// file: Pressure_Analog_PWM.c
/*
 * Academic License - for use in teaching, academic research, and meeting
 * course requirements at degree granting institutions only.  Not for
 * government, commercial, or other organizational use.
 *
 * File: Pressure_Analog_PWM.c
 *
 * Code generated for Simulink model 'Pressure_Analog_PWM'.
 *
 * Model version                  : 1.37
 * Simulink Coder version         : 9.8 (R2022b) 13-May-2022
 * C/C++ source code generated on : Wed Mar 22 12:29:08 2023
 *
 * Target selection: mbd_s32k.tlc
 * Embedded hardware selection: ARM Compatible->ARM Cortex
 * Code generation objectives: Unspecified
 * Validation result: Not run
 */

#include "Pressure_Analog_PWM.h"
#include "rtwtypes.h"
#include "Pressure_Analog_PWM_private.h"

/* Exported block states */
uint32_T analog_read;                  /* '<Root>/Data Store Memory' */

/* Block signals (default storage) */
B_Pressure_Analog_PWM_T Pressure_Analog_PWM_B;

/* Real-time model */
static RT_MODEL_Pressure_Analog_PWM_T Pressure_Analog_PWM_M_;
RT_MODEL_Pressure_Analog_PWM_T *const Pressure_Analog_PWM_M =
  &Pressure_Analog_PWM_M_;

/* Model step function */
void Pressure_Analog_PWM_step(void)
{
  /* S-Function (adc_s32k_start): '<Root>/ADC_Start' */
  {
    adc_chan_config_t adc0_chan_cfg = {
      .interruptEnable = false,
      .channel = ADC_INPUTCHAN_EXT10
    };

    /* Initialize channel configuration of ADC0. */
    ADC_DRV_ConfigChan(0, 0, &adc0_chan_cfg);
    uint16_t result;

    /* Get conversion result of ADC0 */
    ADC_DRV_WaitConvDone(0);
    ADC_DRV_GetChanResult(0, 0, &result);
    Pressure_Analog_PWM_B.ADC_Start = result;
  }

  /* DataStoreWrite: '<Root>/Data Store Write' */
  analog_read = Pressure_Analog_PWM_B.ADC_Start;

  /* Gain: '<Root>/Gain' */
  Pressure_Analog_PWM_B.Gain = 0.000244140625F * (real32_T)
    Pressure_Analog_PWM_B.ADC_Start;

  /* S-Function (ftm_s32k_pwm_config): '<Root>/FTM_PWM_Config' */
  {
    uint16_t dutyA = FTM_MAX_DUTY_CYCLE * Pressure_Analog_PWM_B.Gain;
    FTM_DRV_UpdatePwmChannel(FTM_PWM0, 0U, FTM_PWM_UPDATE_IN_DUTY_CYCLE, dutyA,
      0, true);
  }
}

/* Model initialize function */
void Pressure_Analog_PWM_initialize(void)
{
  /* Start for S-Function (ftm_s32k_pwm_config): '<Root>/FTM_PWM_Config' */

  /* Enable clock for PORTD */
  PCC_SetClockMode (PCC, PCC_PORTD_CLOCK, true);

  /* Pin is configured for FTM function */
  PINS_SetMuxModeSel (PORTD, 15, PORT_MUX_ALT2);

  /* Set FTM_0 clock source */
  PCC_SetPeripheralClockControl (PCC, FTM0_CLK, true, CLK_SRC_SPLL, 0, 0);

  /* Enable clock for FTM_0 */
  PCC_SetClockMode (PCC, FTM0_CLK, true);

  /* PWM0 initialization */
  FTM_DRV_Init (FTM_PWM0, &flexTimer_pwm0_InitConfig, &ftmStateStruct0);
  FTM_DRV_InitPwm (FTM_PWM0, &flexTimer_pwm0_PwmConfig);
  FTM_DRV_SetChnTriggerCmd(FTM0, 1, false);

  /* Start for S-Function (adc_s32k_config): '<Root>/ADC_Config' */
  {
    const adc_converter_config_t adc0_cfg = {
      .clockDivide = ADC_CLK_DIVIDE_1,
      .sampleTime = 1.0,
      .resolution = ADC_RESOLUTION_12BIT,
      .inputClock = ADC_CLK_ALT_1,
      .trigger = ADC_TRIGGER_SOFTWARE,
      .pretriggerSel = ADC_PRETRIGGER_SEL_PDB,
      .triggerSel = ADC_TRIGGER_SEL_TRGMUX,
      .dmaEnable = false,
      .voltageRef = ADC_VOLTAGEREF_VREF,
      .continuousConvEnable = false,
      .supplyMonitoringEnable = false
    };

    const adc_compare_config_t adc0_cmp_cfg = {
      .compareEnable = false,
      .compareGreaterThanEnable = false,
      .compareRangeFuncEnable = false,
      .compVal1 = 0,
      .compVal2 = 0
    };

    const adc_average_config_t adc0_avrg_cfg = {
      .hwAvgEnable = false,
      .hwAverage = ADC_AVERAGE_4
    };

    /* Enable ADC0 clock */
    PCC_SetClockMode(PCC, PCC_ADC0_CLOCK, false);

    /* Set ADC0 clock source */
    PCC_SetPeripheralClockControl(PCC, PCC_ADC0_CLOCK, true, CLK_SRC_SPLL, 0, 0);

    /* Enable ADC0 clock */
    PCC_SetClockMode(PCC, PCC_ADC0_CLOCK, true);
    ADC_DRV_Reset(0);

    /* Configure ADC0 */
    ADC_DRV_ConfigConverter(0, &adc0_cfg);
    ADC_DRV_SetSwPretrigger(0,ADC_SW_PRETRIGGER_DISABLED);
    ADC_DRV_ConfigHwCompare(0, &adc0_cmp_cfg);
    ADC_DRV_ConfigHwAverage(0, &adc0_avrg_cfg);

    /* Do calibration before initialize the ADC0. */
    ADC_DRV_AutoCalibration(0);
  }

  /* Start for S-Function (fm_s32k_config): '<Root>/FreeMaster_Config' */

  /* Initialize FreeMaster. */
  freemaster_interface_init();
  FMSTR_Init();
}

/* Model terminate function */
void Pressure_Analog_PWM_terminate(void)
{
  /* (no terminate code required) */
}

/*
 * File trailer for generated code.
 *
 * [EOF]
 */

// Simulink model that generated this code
simulink model "Pressure_Analog_PWM"  (R2022b)
settings: Solver=FixedStepDiscrete  StartTime=0.0  StopTime=10.0  RelTol=1e-3  EnableMultiTasking=on
InitFcn:
  | mbd_s32k_consistency_checks(bdroot(gcs));
model workspace (MAT data in the model file):
  mwTaskManagerKernelLatency = 1e-06
undefined symbols (not defined in the file): LQFP
libraries: mbd_s32k1xx_ec_toolbox x5

== system Pressure_Analog_PWM ==
  note: This algorithm reads the analog output from the pressure
      | sensor and changes the red LED intensity accordingly.
      | The read value can be visualized on FreeMaster through
      |  the variable "analog_read".
      |
      | Hardware Requirements:
      | - S32K144 board
      | - HTDM100BSP
      |
      | Pin connections:
      |
      | Sensor    |     Board
      |     1         |      PTC2
      |     2         |      GND
      |     3         |        5V
      |
      |
      | Kamilla Peixoto - Scaleo Medical
      | v1 - 22/03/2023
  note: Analog Reading
  note: Watched Variables
  note: Configuration
  ADC_Config : mbd_s32k1xx_ec_toolbox/Motor Control Blocks/ADC Blocks/ADC_Config  instance=0  mode=12-bit conversion  smplts=2  adiclk=alternate clock 1  adiv=input clock  show_adv_opts=on  pretrgsel=PDB pre-trigger  swpretrg=Disabled  adtrg=software  trgsel=TRGMUX output  refsel=Vrefh and Vrefl  supply_monitoring=off  acfe=off  acfgt=off  acren=off  cv1=0  cv2=0  adco=off  avge=off  avgs=4 samples
  ADC_Start : mbd_s32k1xx_ec_toolbox/Motor Control Blocks/ADC Blocks/ADC_Start  instance=0  adc_r=A  adc_chan=PTC2: [ADC0_SE10 | ADC Single Ended Input]  aien=off  mcuTargetUpdate=on
  Data Store Memory : DataStoreMemory  DataStoreName=analog_read  WriteAfterWriteMsg=warning  ShowAdditionalParam=off  StateMustResolveToSignalObject=on
  Data Store Write : DataStoreWrite  DataStoreName=analog_read  IndexOptions=Index vector (dialog)  Indices=1  OutputSizes=1
  FTM_PWM_Config : mbd_s32k1xx_ec_toolbox/Motor Control Blocks/FTM Blocks/FTM_PWM_Config  ftmModule=0  ftmMode=Edge-Aligned PWM  ftmSourceClock=80 MHz  swcontrol_enable=off  chan0En=on  chan0Type=Complementary  chan2En=off  chan2Type=Independent  chan4En=off  chan4Type=Independent  chan6En=off  chan6Type=Independent  ftmPwmUnits=Hz  outFrequency=10000  ftmPeriod=8000  ftmPrescaler=Divide by 1  deadtimeUnits=Nanoseconds  deadtimeNs=0  deadtimeTicks=0  deadtimePrescaler=Divide by 1  dutyCycleCh0=0.25  dutyCycleCh1=0.25  dutyCycleCh2=0.25  dutyCycleCh3=0.25  dutyCycleCh4=0.25  dutyCycleCh5=0.25  dutyCycleCh6=0.25  dutyCycleCh7=0.25  dutyCycleSim=off  startAfterInit=on  showAdvOpt=on  pinFtmCh0=PTD15: [FTM0_CH0 | FTM Channel]  pinFtmCh1=None  pinPolCh0=Active Low  pinPolCh1=Active Low  outputComplem0=Main duplicated  outputLevel0=Low  outputLevel1=Low  pinFtmCh2=PTD0: [FTM0_CH2 | FTM Channel]  pinFtmCh3=None  pinPolCh2=Active Low  pinPolCh3=Active Low  outputComplem2=Main duplicated  outputLevel2=Low  outputLevel3=Low  pinFtmCh4=PTB4: [FTM0_CH4 | FTM Channel]  pinFtmCh5=None  pinPolCh4=Active Low  pinPolCh5=Active Low  outputComplem4=Main duplicated  outputLevel4=Low  outputLevel5=Low  pinFtmCh6=PTA17: [FTM0_CH6 | FTM Channel]  pinFtmCh7=None  pinPolCh6=Active Low  pinPolCh7=Active Low  outputComplem6=Main duplicated  outputLevel6=Low  outputLevel7=Low  initTrigger=off  chTrigger0=off  chTrigger1=off  chTrigger2=off  chTrigger3=off  chTrigger4=off  chTrigger5=off  chTrigger6=off  chTrigger7=off  mcuTargetUpdate=on  pwmSyncTrg=Software trigger  pwmSyncHwRouting=TRGMUX_FTM7  pwmSyncTrg0=off  pwmSyncTrg1=off  pwmSyncTrg2=off  pwmSyncAutoClear=on  pwmSyncMinLoad=on  pwmSyncMaxLoad=on  pwmSyncInvert=System Clock  pwmSyncOutControl=System Clock  pwmSyncOutMask=System Clock  pwmSyncCounterInitial=System Clock  pwmSyncPoints=Update now  reloadEnable=off  reloadPriority=15  reloadHalfCycle=off  reloadHCR=0  reloadFrequency=0  chnMatch0=off  chnMatch1=off  chnMatch2=off  chnMatch3=off  chnMatch4=off  chnMatch5=off  chnMatch6=off  chnMatch7=off  pwmFaultProtection=off  pwmFaultInterrupt=off  pwmFaultClearing=Fault control disabled  pwmFaultPinState=Safe Value  pwmFaultFilterValue=0  pwmFaultPriority=15  fault_disen_0=off  fault_filter_0=off  fault_polarity_0=Active High  fault_disen_1=off  fault_filter_1=off  fault_polarity_1=Active high  fault_disen_2=off  fault_filter_2=off  fault_polarity_2=Active high  fault_disen_3=off  fault_filter_3=off  fault_polarity_3=Active high  fault_pin_0=None  fault_pin_1=None  fault_pin_2=None  fault_pin_3=None
  FreeMaster_Config : mbd_s32k1xx_ec_toolbox/Utility Blocks/FreeMaster_Config  interface=LPUART1  baudrate=115200  rxd=PTC6: [LPUART1_RX | Receive]  txd=PTC7: [LPUART1_TX | Transmit]  mode=Poll-driven  isr_prio=15  show_adv_opts=on  use_scope=on  max_scope_vars=8  use_recorder=on  max_rec_vars=8  rec_buff_size=1024  rec_timebase=0 seconds  comm_buffer_size_auto=on  comm_buffer_size=255  comm_rqueue_size_default=on  comm_rqueue_size=32
  Gain : Gain  Gain=2^(-12)  ParamDataTypeStr=single
  MBD_S32K14x_Config_Information : mbd_s32k1xx_ec_toolbox/MBD_S32K1xx_Config_Information  Priority=0  mbdt_ver=0  disp_str=|  config_params=[]  mcu_target_name=S32K144  mcu_target_package=100-LQFP  mcu_target_sram_size=64KB  mcu_system_clock_freq=80  mcu_xtal_freq=External 8  mcu_steptick_timer=LPIT Channel 0  mcu_steptick_prio=15  ds_import_enable=on  target_compiler=GCC  target_memory=FLASH  gcc_target_compile_opts=-mcpu=cortex-m4 -mthumb -mfloat-abi=hard -mfpu=fpv4-sp-d16 -O1 -g -gstrict-dwarf  gcc_target_assemble_opts=-mcpu=cortex-m4 -mthumb -mfloat-abi=hard -mfpu=fpv4-sp-d16 -g  gcc_target_link_opts=-mcpu=cortex-m4 -mthumb -mfloat-abi=hard -mfpu=fpv4-sp-d16  gcc_target_default_lcf=on  gcc_target_user_lcf=S32K148_192_flash.ld  ghs_target_compile_opts=-cpu=cortexm4f -thumb -DARM_MATH_CM4 -fpu=vfpv4_d16 -fsingle -Ogeneral -Wundef -Wimplicit-int -Wshadow -Wtrigraphs --no_commons --gnu_asm -gnu99 -gdwarf-2 -G  ghs_target_assemble_opts=-cpu=cortexm4f -fpu=vfpv4_d16  ghs_target_link_opts=-cpu=cortexm4f -thumb -fpu=vfpv4_d16  ghs_target_default_lcf=off  ghs_target_user_lcf=S32K148_192_flash.ld  iar_target_compile_opts=--cpu=Cortex-M4F --thumb --fpu=VFPv4_sp -Ol -e --debug --dlib_config normal  iar_target_assemble_opts=--cpu Cortex-M4F --thumb --fpu VFPv4_sp  iar_target_link_opts=--no_exceptions --vfe --inline  iar_target_default_lcf=off  iar_target_user_lcf=S32K148_192_flash.icf  pil_download_enable=off  rbl_download_enable=on  rbl_start_delay=5000000  rbl_download_interface=OpenSDA  rbl_restart_request=off  rbl_com_port=Custom  rbl_com_port_custom=COM1  pil_download_rate=57600  pil_opensda_drive=D: EVB-S32K144  pil_opensda_drive_custom=D  pil_uart_instance=1  pil_uart_rx=PTC6: [LPUART1_RX | Receive]  pil_uart_tx=PTC7: [LPUART1_TX | Transmit]  FTM_PWM_PcrCheckEnDis=on  FTM_Input_Edge_Inputs_PcrCheckEnDis=on  FTM_Dual_Edge_Inputs_PcrCheckEnDis=on  FTM_Quadrature_Inputs_PcrCheckEnDis=on  FTM_Hall_Sensor_Inputs_PcrCheckEnDis=on  LPTMR_PcrCheckEnDis=on  PIT_PcrCheckEnDis=on  RTC_PcrCheckEnDis=on  FlexCAN_PcrCheckEnDis=on  LIN_PcrCheckEnDis=on  FlexIO_PcrCheckEnDis=on  LPI2C_PcrCheckEnDis=on  LPSPI_PcrCheckEnDis=on  LPUART_PcrCheckEnDis=on  CMP_PcrCheckEnDis=on  GPIO_OutputPcrCheckEnDis=on  GPIO_InputPcrCheckEnDis=on  SBC_PcrCheckEnDis=on  BMS_PcrCheckEnDis=on  AMMCLIB_PcrCheckEnDis=on  FM_PcrCheckEnDis=on  Profile_PcrCheckEnDis=on  ConfigParams_PcrCheckEnDis=on  ModelRef_PcrCheckEnDis=on  PDB0_PcrCheckEnDis=on  CSEc_PcrCheckEnDis=on  eDMA_PcrCheckEnDis=on  FLASH_PcrCheckEnDis=on  ADC_PcrCheckEnDis=on  WDOG_PcrCheckEnDis=on
      | Target : S32K144-64KB_SRAM
      | Package : 100-pin
      | System clock : 80 MHz
      | XTAL clock : External 8 MHz
      | Compiler : GCC
      | Target Type : FLASH
      | Download Code after build : (OpenSDA: E)
      | Step Tick Interrupt Priority : 15
  wires:
  ADC_Start/1 -> Data Store Write/1, Gain/1
  Gain/1 -> FTM_PWM_Config/1
